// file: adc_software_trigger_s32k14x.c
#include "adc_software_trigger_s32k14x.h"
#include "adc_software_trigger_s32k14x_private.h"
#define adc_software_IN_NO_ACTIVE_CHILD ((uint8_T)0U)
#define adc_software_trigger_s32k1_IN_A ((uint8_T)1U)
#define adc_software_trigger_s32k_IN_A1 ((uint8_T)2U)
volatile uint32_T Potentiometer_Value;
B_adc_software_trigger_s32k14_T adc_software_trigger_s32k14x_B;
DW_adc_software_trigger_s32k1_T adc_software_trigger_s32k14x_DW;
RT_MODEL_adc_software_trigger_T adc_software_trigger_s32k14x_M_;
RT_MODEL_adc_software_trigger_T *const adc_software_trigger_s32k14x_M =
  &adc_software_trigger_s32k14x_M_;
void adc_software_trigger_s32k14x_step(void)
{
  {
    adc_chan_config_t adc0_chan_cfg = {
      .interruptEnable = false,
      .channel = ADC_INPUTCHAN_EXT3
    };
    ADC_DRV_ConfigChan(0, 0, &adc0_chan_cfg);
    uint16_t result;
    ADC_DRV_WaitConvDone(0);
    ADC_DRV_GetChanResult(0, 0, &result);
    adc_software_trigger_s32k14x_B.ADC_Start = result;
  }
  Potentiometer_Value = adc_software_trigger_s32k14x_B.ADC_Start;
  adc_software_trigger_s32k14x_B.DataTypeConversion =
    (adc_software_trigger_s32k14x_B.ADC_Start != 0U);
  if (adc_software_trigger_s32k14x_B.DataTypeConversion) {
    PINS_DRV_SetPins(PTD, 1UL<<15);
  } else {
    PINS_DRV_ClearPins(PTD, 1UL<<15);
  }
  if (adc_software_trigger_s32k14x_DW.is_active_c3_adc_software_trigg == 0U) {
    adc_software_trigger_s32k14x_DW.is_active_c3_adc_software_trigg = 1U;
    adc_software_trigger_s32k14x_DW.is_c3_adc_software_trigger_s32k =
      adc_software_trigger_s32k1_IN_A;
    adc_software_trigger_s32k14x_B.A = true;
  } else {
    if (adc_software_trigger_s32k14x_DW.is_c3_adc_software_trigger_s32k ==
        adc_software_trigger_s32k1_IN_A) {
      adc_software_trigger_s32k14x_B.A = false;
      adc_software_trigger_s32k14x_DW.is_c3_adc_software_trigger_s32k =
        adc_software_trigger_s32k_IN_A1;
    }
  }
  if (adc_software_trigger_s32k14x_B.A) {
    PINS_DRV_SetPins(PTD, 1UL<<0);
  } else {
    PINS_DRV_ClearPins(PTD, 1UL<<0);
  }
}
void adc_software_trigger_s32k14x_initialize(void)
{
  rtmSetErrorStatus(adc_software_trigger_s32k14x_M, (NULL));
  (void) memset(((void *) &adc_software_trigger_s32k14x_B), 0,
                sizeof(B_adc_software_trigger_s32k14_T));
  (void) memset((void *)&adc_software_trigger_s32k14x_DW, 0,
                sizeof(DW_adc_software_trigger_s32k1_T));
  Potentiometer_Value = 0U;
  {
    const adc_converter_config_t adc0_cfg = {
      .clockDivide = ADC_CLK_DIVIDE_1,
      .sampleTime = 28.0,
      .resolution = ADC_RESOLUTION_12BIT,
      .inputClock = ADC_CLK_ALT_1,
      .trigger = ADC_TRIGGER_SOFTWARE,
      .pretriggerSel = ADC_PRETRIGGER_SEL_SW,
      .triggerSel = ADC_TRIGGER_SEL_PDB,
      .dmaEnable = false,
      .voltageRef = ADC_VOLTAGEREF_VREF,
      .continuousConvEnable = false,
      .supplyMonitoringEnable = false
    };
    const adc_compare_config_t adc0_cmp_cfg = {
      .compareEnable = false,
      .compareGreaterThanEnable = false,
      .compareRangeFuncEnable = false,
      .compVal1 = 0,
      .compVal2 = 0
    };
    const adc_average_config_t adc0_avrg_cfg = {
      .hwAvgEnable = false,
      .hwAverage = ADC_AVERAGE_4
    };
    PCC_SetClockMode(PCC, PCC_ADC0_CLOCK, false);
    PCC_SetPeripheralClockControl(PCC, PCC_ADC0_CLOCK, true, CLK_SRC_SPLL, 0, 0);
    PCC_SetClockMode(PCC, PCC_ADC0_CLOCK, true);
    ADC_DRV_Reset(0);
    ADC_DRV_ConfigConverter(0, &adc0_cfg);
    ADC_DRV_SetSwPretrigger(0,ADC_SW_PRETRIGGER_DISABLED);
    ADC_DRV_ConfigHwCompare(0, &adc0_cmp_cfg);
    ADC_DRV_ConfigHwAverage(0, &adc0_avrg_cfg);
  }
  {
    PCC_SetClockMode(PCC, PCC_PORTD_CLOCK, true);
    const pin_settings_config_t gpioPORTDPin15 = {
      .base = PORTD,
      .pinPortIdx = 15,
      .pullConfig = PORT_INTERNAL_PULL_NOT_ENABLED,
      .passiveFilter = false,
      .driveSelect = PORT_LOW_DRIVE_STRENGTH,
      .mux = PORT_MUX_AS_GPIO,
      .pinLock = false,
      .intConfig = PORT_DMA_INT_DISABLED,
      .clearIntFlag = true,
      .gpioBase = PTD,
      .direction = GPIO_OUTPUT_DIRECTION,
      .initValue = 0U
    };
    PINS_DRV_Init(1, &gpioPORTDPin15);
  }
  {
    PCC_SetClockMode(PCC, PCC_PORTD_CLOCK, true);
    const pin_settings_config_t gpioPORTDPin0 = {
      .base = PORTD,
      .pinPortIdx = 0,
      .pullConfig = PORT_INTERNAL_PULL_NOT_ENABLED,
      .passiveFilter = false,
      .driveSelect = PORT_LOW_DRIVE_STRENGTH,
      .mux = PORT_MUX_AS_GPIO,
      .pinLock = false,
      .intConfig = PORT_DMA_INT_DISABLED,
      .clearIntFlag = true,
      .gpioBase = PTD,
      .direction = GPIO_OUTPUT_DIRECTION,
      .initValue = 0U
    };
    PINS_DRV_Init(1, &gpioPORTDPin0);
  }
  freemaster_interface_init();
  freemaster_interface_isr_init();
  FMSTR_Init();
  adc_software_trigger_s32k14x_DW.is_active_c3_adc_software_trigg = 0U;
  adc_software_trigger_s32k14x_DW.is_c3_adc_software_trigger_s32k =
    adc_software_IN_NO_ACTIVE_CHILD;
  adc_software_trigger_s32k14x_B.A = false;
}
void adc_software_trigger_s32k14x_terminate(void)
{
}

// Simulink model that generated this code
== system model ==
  DataStoreWrite#1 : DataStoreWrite  DataStoreName=Potentiometer_Value  <- 1: ADC_Start
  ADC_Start : mbd_s32k1xx_ec_toolbox/Motor Control Blocks/ADC Blocks/ADC_Start
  Digital_Output#1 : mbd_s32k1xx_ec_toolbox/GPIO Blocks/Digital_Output  <- 1: DataTypeConversion
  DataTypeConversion : DataTypeConversion  <- 1: ADC_Start
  Digital_Output#2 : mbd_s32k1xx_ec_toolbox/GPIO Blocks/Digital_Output  <- 1: Stateflowchart#1
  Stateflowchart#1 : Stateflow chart
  ADC_Config#1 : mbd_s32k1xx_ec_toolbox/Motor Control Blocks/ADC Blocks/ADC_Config
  FreeMaster_Config#1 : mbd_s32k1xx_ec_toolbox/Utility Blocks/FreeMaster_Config
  DataStoreMemory#1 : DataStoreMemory  DataStoreName=Potentiometer_Value
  MBD_S32K1xx_Config_Information#1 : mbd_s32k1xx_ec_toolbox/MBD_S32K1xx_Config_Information
== stateflow chart Stateflowchart#1 ==
  state A
  state A1
  (default) -> A
  A -> A1
  data: A output boolean [0..1]
